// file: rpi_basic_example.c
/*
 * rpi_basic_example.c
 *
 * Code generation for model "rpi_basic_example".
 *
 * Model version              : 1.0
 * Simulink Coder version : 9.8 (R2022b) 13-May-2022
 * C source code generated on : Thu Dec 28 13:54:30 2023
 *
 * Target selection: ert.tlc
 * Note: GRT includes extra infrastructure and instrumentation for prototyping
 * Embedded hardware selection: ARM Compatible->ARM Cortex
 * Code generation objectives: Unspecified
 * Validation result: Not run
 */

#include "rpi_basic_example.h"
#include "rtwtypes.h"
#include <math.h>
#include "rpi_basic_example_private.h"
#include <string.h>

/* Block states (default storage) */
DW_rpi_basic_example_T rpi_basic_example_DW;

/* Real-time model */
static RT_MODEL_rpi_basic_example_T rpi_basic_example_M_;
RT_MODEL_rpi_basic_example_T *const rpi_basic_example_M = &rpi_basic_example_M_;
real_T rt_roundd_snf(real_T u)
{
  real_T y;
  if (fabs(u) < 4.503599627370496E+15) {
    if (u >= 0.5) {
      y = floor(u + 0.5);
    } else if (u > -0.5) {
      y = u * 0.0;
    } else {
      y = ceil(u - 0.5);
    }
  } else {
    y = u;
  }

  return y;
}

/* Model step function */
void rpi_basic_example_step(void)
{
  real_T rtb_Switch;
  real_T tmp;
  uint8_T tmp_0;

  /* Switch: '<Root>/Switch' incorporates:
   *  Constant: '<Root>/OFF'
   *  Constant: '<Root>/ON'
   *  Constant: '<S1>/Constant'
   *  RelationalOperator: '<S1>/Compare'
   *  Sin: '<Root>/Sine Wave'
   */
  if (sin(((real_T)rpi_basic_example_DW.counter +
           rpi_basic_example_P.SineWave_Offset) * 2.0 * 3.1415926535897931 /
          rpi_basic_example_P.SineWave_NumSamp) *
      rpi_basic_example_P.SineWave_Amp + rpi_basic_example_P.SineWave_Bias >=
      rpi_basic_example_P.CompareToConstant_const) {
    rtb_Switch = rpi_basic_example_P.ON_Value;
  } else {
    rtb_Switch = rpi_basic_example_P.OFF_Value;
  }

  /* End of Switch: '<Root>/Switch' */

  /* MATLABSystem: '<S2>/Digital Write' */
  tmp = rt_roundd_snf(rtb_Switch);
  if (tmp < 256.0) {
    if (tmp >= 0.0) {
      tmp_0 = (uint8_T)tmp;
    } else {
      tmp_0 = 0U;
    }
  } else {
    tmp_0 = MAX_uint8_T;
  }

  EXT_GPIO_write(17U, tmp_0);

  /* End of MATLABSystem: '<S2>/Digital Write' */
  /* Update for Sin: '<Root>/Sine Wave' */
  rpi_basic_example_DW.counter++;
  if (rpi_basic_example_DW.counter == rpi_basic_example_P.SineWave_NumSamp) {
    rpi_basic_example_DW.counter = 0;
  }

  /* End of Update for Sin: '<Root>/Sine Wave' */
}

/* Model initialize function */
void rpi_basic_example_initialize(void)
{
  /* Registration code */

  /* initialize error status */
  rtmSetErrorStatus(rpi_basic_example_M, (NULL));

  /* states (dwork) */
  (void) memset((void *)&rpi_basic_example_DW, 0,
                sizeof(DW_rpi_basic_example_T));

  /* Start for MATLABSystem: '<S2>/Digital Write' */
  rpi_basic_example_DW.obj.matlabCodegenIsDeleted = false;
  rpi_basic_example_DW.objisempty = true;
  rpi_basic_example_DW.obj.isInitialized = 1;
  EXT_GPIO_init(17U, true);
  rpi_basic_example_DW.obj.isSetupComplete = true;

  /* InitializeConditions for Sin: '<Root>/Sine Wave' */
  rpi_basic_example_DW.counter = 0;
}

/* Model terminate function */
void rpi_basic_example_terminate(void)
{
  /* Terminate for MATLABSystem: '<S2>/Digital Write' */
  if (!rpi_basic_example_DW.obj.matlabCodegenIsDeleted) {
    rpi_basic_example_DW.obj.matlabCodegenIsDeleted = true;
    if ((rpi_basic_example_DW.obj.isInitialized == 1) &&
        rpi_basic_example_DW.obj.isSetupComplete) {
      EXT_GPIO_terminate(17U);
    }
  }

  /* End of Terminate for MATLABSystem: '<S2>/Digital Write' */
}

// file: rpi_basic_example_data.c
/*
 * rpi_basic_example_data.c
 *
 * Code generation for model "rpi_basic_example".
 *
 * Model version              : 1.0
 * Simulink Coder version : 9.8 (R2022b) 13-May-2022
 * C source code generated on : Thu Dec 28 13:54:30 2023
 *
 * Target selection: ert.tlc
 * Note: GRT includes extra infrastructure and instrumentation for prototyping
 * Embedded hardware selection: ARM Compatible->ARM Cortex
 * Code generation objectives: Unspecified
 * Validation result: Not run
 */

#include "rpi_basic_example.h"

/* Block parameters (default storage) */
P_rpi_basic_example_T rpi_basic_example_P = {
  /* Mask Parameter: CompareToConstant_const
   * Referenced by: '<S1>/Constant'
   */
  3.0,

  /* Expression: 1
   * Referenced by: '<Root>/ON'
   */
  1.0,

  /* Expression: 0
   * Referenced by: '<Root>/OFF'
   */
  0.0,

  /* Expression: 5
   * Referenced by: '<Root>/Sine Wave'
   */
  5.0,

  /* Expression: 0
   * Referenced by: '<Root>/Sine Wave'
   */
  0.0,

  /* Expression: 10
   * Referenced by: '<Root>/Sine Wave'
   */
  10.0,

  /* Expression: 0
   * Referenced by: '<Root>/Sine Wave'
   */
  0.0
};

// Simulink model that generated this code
simulink model "rpi_basic_example"  (R2022b)
settings: Solver=ode3  StartTime=0.0  StopTime=10  RelTol=1e-3  EnableMultiTasking=on
libraries: simulink x1, embedlinuxBasiclib x1

== system rpi_basic_example ==
  note: Deployment
  note: Simulation
  note: Add Simulation Sources
  note: Project Title: <Your project name here>
  note: Organizing functionality as color-coded areas makes block diagrams descriptive and helps to develop increasingly complex algorithms.
  note: Add RaspberryPi Sensors & Inputs
  note: Design your algorithm here
  note: Add Display and Visualization
  note: Add RaspberryPi Actuators & Outputs
  note: Use this model to design an algorithm to toggle a GPIO pin on the Raspberry Pi Hardware.
      |
      | Getting Started:
      |
      | Add Simulation Sources blocks from:
      | Simulink Library
      | Add Raspberry Pi Sensors, Inputs and Actuator blocks from:
      | Raspberry Pi Library
      |
      | Configure Raspberry Pi Hardware:
      |
      | Open Model Configuration Parameters dialog
      | Under the Hardware Implementation option, select the Raspberry Pi hardware from the Hardware board parameter list.
      |
      | Simulate the Model
      |
      | Click the Run button on the Simulink Editor toolbar.
      |
      | Run the Model on Raspberry Pi Hardware
      |
      | In the Hardware tab, click Build, Deploy & Start
      |
      | Other Things to Try:
      |
      | Create and run a model that repeatedly brightens and dims an LED. Hint: Use PWM block as an Raspberry Pi actuator.
  Compare To Constant : simulink/Logic and Bit Operations/Compare To Constant  relop=>=  const=3  OutDataTypeStr=boolean
  GPIO Write : embedlinuxBasiclib/GPIO Write  board=Model B+  gpio=17  direction=Output  blockPlatform=Raspberry Pi
  OFF : Constant  Value=0  SampleTime=-1
  ON : Constant  SampleTime=-1
  Run Demo1 : Subsystem  Description=Controls host-side RTDX processing.
  Scope : Scope
  Sine Wave : Sin  SineType=Sample based  Amplitude=5  SampleTime=0.1
  Switch : Switch  Criteria=u2 > Threshold  SaturateOnIntegerOverflow=off  InputSameDT=off
  wires:
  Sine Wave/1 -> Compare To Constant/1
  OFF/1 -> Switch/3
  Switch/1 -> GPIO Write/1, Scope/1
  ON/1 -> Switch/1
  Compare To Constant/1 -> Switch/2

== system rpi_basic_example/Run Demo1 ==
